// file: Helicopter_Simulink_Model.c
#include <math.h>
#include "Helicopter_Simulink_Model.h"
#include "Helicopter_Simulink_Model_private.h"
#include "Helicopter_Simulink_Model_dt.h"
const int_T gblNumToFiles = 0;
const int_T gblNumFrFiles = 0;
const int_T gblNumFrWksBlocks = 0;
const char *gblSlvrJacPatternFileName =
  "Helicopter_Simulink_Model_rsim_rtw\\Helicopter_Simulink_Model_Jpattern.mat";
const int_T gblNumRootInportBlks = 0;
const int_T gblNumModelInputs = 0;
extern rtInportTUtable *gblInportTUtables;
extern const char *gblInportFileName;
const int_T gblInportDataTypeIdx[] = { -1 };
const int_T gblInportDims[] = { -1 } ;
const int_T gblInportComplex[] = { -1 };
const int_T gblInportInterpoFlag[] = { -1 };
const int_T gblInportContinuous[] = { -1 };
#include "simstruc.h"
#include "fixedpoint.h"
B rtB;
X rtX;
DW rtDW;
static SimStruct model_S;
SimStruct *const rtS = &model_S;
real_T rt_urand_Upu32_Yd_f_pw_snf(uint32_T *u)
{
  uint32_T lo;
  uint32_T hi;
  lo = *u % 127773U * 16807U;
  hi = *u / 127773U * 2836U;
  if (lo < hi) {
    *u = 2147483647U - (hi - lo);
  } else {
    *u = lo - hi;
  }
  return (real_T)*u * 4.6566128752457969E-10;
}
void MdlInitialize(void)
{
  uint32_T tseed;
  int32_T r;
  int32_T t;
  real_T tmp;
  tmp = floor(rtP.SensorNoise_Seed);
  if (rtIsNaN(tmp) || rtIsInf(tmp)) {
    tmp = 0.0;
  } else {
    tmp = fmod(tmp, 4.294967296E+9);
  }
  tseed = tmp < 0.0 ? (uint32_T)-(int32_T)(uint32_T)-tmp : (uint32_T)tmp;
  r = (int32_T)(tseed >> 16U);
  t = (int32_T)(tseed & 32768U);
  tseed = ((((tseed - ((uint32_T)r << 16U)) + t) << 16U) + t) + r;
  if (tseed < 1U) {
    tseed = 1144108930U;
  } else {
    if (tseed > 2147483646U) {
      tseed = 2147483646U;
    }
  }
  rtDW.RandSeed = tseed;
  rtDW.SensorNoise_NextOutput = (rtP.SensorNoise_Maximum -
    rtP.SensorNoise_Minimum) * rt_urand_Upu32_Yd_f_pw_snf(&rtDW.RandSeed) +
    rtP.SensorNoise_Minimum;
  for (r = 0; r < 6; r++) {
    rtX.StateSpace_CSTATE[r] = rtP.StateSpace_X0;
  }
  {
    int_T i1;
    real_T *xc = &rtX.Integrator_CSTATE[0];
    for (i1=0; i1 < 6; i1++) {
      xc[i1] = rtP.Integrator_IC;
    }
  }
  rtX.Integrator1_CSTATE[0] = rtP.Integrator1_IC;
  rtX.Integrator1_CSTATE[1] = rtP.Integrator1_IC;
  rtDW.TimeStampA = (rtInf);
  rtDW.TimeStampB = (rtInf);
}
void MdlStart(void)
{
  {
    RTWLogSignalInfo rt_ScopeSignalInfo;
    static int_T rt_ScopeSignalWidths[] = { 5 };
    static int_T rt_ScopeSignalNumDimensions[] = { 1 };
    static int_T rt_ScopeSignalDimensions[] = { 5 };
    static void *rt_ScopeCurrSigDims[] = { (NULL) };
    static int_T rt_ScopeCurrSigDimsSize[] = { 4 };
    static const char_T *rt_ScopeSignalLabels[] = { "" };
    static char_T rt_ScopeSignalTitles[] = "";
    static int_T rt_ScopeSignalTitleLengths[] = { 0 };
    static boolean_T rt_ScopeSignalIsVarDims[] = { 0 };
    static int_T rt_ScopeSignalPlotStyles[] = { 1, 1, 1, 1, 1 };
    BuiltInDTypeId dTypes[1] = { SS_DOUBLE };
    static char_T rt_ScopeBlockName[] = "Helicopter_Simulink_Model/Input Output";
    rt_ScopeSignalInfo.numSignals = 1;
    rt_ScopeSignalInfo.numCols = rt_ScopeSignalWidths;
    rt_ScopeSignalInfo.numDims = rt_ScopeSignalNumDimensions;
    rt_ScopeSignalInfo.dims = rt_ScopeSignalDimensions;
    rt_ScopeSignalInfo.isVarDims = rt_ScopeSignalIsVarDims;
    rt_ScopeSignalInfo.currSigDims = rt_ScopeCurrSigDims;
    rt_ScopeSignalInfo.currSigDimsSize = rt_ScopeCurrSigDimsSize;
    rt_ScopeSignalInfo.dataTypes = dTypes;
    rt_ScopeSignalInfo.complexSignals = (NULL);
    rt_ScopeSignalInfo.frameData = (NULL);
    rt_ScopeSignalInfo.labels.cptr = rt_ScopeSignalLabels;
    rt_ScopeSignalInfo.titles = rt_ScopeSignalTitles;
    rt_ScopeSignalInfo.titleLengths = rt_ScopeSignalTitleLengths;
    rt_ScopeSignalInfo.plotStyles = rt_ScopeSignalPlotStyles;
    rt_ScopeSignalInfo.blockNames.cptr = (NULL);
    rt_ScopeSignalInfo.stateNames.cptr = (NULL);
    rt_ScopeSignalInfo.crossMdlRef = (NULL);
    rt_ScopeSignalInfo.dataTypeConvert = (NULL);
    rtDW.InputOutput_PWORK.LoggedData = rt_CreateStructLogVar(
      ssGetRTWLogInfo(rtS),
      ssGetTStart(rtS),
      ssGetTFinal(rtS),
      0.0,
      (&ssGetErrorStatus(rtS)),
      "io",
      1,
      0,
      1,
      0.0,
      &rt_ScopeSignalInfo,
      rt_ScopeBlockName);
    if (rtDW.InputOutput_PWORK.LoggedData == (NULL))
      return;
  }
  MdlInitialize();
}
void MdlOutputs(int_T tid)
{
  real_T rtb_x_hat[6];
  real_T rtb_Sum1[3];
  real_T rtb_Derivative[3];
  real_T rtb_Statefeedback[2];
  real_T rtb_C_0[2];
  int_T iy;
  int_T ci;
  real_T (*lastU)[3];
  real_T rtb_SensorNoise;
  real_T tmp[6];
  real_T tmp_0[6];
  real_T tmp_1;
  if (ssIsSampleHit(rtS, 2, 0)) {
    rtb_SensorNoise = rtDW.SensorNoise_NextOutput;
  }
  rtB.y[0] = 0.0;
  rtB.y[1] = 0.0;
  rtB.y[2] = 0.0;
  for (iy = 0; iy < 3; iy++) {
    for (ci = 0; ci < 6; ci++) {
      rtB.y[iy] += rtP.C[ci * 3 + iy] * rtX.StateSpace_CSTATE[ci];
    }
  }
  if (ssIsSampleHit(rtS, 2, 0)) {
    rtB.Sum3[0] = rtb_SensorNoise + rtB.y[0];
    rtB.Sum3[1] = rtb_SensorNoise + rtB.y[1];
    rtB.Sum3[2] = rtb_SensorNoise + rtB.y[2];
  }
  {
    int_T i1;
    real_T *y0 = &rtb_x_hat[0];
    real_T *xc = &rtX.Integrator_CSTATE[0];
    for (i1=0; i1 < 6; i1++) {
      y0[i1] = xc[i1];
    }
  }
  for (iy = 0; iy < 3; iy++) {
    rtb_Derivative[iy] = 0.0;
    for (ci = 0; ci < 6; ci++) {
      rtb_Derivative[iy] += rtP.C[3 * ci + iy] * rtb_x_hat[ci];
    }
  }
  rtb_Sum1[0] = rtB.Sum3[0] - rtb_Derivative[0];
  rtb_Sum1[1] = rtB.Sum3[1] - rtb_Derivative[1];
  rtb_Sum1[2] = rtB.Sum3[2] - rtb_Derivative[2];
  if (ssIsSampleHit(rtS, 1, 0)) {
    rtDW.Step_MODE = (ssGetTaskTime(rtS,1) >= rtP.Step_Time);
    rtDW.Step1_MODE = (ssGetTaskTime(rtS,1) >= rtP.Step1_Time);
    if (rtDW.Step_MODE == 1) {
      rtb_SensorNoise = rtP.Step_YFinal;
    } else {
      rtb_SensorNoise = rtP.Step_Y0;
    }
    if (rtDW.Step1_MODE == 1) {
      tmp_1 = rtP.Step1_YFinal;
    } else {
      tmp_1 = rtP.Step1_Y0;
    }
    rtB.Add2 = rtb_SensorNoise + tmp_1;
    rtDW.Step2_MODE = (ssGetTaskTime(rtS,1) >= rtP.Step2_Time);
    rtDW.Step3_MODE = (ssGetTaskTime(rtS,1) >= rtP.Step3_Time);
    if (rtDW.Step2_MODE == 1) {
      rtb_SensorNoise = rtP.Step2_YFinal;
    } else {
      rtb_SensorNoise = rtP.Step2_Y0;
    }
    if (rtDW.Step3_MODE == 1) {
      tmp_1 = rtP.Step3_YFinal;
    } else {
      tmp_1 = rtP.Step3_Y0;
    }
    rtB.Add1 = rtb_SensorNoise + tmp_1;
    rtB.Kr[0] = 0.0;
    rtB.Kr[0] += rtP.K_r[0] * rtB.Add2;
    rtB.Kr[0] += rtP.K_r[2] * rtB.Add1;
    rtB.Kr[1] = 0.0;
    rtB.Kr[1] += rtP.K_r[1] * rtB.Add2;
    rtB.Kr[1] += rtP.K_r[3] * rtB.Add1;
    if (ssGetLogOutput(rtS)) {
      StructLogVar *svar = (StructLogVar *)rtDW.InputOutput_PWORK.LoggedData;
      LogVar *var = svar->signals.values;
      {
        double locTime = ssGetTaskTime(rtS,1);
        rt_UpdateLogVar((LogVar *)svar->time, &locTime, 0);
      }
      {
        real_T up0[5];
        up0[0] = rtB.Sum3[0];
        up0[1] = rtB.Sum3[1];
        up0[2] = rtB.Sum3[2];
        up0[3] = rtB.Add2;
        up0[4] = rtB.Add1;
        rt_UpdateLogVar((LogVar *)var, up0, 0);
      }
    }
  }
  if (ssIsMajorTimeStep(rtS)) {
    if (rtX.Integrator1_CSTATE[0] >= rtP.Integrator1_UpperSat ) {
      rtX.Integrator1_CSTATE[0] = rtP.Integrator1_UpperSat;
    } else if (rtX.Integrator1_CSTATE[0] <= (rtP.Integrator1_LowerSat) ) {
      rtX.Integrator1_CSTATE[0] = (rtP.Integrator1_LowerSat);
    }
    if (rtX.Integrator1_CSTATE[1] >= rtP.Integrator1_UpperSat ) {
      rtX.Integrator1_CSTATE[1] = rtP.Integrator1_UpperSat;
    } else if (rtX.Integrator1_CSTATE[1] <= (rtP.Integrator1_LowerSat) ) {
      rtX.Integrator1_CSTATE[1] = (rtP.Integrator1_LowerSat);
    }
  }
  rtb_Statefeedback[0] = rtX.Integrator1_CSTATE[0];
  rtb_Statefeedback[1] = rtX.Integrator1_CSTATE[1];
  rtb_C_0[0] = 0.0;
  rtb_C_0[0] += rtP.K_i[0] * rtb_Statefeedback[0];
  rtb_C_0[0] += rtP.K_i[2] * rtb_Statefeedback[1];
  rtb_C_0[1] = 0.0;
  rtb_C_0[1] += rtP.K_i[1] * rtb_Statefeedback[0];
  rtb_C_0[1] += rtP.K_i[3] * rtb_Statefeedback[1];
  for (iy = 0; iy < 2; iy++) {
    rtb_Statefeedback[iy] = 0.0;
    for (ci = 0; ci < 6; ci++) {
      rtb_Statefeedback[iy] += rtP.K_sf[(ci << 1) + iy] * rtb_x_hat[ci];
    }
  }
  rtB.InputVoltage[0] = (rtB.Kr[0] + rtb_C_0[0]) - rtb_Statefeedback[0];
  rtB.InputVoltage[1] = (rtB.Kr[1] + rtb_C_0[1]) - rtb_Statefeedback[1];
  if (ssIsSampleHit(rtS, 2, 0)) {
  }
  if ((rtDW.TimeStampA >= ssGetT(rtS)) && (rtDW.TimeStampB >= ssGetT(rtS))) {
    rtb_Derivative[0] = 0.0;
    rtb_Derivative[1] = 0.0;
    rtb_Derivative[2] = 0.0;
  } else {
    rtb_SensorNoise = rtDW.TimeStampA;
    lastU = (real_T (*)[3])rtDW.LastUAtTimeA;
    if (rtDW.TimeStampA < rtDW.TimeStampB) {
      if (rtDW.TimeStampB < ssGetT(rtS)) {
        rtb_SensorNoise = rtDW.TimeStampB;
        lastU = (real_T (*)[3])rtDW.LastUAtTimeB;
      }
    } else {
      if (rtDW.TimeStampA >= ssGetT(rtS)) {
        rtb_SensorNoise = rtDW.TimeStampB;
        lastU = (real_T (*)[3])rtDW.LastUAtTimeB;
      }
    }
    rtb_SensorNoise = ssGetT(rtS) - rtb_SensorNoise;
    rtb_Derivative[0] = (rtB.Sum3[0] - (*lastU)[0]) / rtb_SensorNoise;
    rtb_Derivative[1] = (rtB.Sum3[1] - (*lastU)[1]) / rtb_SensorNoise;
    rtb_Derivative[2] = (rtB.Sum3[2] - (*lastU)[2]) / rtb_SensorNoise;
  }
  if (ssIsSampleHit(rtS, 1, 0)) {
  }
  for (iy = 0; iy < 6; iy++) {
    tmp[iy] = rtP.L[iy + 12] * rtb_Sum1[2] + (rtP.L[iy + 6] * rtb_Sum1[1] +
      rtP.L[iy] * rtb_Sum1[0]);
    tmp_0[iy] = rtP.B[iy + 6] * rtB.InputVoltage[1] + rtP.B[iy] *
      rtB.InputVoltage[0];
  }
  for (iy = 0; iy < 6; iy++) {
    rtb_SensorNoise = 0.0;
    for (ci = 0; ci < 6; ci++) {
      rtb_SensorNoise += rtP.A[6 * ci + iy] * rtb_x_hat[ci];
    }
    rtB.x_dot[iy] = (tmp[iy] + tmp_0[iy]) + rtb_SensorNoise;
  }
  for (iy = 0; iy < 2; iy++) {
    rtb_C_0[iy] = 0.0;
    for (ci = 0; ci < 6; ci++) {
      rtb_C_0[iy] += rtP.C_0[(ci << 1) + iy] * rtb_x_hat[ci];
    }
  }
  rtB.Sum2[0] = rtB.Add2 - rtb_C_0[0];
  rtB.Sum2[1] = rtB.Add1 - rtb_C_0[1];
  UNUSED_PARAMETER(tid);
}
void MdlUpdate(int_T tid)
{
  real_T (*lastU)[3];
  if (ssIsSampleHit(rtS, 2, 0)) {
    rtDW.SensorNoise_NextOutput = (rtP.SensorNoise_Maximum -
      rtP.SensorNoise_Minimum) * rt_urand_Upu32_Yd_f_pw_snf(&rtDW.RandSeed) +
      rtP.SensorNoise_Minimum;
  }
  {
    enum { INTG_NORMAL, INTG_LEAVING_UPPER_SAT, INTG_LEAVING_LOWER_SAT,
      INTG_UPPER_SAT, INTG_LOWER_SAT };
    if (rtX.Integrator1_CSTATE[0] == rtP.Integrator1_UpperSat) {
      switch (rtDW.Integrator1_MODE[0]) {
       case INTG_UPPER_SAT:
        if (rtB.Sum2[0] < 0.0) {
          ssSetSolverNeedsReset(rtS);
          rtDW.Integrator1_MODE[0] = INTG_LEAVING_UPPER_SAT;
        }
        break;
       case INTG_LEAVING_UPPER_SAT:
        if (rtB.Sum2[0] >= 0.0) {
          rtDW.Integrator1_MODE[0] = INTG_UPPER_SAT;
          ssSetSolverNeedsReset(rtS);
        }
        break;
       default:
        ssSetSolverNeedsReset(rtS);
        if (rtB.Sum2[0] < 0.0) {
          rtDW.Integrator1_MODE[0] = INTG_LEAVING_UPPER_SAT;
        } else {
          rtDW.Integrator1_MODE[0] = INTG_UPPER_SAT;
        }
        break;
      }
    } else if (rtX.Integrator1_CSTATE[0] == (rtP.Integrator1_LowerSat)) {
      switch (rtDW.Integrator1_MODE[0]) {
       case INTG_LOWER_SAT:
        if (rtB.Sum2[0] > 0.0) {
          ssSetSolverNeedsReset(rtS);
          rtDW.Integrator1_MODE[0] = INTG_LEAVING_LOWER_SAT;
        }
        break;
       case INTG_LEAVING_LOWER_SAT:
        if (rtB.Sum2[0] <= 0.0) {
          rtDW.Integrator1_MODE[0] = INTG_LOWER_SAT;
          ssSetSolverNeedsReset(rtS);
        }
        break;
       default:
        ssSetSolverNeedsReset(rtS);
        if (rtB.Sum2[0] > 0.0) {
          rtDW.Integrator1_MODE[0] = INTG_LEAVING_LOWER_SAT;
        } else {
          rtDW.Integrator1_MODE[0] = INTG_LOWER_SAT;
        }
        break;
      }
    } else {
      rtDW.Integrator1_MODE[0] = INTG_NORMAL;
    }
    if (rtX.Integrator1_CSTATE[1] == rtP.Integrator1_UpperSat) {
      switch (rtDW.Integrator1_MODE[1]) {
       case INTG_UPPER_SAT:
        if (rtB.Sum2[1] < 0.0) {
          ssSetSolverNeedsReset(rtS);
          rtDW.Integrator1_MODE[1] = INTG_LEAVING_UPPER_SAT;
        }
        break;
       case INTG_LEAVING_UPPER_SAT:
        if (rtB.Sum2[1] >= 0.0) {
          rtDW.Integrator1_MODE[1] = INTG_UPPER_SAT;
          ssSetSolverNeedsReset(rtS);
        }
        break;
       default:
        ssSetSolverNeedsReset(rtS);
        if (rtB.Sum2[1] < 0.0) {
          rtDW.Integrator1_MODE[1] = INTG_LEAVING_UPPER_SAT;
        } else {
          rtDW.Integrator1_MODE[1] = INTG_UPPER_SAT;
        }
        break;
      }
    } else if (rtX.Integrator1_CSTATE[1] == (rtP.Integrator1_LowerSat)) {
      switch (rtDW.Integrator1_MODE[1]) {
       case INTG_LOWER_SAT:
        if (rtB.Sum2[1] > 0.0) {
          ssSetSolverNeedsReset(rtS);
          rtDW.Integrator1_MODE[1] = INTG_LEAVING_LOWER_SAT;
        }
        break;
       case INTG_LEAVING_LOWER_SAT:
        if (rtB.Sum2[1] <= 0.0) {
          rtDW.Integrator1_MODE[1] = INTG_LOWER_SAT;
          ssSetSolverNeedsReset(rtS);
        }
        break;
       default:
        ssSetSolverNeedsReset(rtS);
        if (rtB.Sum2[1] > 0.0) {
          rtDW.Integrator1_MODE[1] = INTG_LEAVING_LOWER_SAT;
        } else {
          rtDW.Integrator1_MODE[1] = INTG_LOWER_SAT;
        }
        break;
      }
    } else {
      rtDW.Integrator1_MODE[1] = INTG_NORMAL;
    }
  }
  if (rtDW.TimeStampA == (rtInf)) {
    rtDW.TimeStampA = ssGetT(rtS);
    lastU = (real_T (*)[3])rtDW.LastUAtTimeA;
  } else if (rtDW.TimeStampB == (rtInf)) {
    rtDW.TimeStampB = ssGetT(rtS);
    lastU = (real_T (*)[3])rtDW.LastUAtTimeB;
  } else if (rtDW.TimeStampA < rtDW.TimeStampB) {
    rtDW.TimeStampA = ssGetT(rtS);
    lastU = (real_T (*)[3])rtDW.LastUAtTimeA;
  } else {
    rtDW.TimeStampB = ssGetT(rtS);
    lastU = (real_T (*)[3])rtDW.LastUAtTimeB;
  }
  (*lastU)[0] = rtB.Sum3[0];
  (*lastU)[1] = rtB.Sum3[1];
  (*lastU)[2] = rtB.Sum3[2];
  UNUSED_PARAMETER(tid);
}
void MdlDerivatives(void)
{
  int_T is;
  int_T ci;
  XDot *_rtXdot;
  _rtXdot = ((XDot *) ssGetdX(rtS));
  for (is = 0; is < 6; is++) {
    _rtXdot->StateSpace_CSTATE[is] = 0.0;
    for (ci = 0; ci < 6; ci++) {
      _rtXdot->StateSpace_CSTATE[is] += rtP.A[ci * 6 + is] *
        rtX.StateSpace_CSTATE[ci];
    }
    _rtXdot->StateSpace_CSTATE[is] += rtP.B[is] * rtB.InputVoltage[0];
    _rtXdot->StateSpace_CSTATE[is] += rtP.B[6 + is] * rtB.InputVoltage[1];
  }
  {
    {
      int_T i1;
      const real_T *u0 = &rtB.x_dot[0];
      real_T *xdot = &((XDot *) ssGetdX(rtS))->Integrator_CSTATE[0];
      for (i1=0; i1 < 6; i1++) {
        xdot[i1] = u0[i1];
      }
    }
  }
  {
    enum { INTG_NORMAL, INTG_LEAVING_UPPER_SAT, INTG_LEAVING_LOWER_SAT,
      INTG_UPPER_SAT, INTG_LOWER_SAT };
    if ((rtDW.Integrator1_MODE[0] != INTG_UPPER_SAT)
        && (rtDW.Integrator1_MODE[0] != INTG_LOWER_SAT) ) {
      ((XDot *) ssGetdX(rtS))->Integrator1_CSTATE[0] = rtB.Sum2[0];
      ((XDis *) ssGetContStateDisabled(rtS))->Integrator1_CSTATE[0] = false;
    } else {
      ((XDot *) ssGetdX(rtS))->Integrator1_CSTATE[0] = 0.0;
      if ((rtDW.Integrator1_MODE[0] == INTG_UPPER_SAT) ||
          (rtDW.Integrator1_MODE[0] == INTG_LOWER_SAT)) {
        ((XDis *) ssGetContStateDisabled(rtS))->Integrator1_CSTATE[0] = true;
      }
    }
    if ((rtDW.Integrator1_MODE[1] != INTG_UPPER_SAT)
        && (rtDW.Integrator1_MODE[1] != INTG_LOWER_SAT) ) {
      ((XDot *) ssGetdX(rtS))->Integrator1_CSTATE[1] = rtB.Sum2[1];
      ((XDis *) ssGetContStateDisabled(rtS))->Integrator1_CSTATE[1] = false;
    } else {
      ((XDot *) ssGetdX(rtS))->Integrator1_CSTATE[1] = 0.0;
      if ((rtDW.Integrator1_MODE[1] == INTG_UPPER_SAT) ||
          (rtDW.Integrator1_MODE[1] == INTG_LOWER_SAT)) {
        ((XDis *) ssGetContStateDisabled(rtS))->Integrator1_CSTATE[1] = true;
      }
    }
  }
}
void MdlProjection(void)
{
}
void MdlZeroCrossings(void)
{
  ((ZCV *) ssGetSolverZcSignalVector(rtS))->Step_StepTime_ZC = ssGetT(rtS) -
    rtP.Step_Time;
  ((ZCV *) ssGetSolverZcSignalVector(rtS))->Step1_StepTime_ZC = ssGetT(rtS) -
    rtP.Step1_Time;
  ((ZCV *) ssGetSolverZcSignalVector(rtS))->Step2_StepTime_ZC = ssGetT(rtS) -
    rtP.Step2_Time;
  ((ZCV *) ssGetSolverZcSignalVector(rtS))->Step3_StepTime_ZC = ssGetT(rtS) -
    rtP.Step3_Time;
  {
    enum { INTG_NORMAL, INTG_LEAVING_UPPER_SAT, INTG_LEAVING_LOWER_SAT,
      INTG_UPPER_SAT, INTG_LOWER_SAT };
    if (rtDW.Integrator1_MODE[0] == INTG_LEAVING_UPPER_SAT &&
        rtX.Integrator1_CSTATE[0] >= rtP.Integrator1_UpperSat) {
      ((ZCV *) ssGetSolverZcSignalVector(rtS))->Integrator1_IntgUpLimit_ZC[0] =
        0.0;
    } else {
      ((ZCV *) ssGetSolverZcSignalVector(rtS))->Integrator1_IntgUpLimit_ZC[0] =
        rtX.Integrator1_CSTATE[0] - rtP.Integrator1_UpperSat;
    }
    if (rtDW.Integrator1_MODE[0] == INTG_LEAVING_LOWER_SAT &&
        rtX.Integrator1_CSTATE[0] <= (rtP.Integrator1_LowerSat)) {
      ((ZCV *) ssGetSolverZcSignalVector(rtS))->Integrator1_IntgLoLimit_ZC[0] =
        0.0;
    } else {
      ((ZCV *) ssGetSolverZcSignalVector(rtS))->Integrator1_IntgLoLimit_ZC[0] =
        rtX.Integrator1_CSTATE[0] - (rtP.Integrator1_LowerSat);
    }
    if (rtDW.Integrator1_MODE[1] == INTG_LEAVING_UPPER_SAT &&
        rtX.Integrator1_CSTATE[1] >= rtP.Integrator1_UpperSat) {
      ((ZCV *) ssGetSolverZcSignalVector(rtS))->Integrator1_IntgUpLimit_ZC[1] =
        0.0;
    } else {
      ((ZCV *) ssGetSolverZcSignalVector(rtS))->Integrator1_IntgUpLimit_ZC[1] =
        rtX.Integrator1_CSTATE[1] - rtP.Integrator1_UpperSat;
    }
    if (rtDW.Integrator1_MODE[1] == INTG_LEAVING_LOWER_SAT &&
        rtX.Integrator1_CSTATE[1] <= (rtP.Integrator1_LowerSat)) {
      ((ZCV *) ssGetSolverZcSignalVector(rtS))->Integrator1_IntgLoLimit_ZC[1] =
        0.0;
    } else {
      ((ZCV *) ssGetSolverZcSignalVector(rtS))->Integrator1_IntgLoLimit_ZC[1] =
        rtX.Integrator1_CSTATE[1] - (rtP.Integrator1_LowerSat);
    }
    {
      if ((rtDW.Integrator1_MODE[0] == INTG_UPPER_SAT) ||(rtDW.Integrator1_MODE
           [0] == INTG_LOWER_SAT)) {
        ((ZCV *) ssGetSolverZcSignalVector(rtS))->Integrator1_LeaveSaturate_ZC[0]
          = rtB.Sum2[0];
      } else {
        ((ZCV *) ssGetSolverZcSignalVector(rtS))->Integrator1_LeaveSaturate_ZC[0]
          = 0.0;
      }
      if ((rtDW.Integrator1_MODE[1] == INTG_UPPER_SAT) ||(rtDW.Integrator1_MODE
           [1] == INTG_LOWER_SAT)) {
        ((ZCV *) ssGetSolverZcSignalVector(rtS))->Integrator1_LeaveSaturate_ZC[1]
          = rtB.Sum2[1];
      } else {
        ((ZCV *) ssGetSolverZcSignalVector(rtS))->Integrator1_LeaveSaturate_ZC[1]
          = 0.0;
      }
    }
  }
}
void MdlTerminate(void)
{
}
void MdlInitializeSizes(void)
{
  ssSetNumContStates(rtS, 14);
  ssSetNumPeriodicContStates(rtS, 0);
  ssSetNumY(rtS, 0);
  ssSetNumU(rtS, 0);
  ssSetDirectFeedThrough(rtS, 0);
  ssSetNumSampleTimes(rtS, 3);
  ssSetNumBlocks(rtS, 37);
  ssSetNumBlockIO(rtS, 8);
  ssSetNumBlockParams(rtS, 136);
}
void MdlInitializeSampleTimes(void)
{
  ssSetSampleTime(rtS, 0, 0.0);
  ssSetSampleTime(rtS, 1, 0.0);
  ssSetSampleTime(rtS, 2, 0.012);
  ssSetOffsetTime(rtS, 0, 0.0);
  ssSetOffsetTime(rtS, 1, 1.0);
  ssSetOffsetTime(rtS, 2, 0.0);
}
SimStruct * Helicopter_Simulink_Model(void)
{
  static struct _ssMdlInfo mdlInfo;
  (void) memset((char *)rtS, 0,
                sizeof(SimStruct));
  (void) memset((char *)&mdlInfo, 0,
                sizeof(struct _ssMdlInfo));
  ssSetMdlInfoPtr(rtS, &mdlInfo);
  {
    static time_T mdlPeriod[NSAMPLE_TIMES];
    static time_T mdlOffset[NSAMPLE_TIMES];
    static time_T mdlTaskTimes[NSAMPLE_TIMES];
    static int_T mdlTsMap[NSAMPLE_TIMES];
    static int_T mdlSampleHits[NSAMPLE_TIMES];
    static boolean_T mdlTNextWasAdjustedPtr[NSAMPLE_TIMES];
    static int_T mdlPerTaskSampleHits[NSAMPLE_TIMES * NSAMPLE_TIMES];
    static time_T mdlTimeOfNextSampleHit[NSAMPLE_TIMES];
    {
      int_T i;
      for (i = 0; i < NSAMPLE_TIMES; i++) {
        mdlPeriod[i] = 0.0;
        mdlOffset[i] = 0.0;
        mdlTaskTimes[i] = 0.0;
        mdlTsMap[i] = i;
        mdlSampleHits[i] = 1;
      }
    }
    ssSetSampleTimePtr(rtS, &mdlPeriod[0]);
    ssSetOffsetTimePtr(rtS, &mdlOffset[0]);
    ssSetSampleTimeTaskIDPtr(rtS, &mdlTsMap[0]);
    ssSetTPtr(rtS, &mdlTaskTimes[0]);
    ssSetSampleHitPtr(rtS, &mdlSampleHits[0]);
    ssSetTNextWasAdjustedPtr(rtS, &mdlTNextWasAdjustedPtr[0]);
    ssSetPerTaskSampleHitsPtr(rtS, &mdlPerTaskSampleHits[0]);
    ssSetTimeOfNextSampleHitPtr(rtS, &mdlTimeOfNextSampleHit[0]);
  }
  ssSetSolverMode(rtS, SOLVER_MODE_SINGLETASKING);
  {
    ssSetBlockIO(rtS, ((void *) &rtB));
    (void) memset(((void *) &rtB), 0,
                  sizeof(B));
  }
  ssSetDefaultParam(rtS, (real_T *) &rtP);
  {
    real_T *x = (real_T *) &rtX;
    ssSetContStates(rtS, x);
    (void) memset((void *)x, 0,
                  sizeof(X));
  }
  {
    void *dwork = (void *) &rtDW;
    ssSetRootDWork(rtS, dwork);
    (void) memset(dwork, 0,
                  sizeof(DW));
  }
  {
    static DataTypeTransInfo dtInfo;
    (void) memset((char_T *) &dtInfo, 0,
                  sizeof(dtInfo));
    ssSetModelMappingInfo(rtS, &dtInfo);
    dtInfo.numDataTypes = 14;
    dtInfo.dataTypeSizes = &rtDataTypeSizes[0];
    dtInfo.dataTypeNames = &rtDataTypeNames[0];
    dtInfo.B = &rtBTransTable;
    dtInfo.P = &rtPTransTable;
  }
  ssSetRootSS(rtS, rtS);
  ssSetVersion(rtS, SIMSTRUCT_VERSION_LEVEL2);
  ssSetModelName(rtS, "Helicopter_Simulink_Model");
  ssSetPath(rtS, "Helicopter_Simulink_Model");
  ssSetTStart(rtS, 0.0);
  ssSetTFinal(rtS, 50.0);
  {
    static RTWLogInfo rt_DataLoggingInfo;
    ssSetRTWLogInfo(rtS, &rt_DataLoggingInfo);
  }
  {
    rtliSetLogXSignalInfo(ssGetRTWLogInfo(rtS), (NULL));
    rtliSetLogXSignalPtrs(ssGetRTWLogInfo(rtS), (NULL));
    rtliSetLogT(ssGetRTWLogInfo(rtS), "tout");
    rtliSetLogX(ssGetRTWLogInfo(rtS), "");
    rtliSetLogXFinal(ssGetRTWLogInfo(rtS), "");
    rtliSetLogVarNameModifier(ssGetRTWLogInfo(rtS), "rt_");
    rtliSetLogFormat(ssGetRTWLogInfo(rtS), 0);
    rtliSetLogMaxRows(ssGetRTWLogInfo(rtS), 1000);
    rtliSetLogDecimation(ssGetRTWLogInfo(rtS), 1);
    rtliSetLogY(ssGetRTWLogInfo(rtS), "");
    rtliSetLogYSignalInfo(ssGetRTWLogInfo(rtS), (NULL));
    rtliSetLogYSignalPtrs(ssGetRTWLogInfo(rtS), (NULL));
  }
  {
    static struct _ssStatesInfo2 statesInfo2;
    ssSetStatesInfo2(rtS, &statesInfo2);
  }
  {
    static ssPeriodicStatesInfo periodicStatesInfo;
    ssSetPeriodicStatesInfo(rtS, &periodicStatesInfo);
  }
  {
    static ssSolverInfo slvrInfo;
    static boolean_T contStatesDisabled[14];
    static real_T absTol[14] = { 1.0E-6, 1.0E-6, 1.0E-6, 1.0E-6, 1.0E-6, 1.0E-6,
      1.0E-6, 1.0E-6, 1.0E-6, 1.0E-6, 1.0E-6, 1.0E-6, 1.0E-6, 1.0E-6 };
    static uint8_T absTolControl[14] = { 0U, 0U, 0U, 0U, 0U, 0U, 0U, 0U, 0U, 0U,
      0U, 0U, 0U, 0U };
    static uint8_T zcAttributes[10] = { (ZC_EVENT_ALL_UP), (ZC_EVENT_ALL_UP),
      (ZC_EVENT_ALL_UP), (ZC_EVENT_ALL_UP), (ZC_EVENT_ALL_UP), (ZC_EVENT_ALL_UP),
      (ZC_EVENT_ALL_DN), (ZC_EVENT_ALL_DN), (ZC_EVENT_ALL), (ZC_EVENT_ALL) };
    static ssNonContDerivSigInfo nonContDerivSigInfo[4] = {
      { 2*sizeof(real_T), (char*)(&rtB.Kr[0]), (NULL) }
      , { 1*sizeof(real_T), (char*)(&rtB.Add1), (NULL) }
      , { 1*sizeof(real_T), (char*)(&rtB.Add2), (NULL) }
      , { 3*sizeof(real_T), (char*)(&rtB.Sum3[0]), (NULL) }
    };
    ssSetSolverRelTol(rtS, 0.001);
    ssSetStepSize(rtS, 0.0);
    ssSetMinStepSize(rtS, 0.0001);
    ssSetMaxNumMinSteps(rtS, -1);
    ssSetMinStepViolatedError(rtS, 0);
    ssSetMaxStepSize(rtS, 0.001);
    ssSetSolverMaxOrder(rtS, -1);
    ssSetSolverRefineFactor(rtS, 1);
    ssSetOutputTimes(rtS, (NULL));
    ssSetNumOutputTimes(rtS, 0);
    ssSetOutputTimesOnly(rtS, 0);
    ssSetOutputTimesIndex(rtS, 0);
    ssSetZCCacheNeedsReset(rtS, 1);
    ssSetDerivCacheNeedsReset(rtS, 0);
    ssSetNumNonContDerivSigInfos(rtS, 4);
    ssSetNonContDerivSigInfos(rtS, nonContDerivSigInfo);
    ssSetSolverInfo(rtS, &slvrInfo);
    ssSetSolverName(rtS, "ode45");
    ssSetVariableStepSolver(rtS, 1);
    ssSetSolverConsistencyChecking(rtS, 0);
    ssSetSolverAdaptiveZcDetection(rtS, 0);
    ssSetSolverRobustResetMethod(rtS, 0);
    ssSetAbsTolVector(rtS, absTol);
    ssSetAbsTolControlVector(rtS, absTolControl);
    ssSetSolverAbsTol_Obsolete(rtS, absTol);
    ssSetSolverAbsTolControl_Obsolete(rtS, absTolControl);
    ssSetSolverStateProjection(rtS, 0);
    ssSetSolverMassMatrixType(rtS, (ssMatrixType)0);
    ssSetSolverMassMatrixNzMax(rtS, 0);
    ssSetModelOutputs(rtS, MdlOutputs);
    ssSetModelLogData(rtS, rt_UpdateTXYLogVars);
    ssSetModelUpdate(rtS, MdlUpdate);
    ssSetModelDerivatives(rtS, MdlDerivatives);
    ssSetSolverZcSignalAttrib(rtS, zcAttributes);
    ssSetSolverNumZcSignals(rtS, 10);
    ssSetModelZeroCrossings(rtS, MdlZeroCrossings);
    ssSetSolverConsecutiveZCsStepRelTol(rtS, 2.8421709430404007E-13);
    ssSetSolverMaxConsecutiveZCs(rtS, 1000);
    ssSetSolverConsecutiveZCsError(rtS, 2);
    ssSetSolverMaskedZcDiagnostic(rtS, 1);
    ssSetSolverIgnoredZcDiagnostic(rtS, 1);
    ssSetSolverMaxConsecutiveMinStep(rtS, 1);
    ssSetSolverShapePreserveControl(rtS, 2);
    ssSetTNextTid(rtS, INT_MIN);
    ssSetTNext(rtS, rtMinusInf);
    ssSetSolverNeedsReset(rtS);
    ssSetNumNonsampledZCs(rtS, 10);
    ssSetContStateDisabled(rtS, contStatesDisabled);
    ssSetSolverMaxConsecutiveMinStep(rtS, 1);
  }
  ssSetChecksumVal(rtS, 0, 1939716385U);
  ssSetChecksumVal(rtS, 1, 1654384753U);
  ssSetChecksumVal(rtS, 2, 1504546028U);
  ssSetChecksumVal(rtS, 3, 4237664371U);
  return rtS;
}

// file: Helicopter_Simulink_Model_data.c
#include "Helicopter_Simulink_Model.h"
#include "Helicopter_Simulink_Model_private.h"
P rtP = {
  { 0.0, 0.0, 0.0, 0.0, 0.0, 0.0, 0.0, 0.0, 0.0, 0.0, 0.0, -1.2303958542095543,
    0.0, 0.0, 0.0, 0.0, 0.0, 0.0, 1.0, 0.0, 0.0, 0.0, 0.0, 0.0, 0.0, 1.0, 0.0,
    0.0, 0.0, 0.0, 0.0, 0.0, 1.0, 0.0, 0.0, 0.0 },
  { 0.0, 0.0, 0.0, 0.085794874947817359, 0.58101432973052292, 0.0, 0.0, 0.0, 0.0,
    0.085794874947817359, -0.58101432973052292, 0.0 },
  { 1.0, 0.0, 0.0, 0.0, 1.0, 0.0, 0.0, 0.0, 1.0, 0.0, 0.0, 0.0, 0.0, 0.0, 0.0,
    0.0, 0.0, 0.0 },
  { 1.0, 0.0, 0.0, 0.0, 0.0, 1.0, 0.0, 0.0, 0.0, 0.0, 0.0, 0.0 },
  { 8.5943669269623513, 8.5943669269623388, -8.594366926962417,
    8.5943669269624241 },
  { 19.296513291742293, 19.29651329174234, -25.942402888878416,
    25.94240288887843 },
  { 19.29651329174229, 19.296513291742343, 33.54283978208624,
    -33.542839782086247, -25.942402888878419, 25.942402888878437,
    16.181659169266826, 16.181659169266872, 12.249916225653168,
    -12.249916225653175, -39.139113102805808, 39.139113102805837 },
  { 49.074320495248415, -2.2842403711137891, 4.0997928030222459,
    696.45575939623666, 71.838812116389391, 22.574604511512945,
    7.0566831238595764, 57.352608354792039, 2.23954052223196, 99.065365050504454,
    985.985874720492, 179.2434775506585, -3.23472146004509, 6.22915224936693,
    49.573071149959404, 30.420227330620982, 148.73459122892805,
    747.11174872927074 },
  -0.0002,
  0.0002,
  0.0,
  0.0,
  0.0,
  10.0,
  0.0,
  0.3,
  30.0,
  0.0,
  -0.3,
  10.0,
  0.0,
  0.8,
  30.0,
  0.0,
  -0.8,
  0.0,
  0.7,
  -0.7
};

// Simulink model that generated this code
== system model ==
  Derivative : Derivative  <- 1: Sum3
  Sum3 : Sum  Inputs=++  <- 1: SensorNoise, 2: ZeroOrderHold#1
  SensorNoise : UniformRandomNumber
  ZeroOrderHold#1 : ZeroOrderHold  <- 1: StateSpace
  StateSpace : StateSpace  A=A  B=B  C=C  D=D  X0=0  <- 1: Sum#1
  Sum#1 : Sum  Inputs=++-  <- 1: Kr, 2: Gain#1, 3: Statefeedback
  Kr : Gain  Gain=K_r  Multiplication=Matrix(K*u)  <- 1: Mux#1
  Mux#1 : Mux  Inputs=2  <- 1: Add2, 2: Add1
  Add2 : Sum  <- 1: Step, 2: Step1
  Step : Step  Time=10  After=0.3
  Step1 : Step  Time=30  After=-0.3
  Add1 : Sum  <- 1: Step2, 2: Step3
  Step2 : Step  Time=10  After=0.8
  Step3 : Step  Time=30  After=-0.8
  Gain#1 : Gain  Gain=K_i  Multiplication=Matrix(K*u)  <- 1: Integrator1
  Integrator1 : Integrator  LimitOutput=on  UpperSaturationLimit=0.7  LowerSaturationLimit=-0.7  <- 1: Sum2
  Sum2 : Sum  Inputs=+-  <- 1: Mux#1, 2: C_0
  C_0 : Gain  Gain=C_0  Multiplication=Matrix(K*u)  <- 1: Integrator
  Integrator : Integrator  <- 1: Sum#2
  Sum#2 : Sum  Inputs=+++  <- 1: Gain#2, 2: Gain#3, 3: Gain#4
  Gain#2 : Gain  Gain=L  Multiplication=Matrix(K*u)  <- 1: Sum1
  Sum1 : Sum  Inputs=+-  <- 1: Sum3, 2: Gain#5
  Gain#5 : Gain  Gain=C  Multiplication=Matrix(K*u)  <- 1: Integrator
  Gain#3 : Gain  Gain=B  Multiplication=Matrix(K*u)  <- 1: Sum#1
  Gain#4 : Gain  Gain=A  Multiplication=Matrix(K*u)  <- 1: Integrator
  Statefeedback : Gain  Gain=K_sf  Multiplication=Matrix(K*u)  <- 1: Integrator
